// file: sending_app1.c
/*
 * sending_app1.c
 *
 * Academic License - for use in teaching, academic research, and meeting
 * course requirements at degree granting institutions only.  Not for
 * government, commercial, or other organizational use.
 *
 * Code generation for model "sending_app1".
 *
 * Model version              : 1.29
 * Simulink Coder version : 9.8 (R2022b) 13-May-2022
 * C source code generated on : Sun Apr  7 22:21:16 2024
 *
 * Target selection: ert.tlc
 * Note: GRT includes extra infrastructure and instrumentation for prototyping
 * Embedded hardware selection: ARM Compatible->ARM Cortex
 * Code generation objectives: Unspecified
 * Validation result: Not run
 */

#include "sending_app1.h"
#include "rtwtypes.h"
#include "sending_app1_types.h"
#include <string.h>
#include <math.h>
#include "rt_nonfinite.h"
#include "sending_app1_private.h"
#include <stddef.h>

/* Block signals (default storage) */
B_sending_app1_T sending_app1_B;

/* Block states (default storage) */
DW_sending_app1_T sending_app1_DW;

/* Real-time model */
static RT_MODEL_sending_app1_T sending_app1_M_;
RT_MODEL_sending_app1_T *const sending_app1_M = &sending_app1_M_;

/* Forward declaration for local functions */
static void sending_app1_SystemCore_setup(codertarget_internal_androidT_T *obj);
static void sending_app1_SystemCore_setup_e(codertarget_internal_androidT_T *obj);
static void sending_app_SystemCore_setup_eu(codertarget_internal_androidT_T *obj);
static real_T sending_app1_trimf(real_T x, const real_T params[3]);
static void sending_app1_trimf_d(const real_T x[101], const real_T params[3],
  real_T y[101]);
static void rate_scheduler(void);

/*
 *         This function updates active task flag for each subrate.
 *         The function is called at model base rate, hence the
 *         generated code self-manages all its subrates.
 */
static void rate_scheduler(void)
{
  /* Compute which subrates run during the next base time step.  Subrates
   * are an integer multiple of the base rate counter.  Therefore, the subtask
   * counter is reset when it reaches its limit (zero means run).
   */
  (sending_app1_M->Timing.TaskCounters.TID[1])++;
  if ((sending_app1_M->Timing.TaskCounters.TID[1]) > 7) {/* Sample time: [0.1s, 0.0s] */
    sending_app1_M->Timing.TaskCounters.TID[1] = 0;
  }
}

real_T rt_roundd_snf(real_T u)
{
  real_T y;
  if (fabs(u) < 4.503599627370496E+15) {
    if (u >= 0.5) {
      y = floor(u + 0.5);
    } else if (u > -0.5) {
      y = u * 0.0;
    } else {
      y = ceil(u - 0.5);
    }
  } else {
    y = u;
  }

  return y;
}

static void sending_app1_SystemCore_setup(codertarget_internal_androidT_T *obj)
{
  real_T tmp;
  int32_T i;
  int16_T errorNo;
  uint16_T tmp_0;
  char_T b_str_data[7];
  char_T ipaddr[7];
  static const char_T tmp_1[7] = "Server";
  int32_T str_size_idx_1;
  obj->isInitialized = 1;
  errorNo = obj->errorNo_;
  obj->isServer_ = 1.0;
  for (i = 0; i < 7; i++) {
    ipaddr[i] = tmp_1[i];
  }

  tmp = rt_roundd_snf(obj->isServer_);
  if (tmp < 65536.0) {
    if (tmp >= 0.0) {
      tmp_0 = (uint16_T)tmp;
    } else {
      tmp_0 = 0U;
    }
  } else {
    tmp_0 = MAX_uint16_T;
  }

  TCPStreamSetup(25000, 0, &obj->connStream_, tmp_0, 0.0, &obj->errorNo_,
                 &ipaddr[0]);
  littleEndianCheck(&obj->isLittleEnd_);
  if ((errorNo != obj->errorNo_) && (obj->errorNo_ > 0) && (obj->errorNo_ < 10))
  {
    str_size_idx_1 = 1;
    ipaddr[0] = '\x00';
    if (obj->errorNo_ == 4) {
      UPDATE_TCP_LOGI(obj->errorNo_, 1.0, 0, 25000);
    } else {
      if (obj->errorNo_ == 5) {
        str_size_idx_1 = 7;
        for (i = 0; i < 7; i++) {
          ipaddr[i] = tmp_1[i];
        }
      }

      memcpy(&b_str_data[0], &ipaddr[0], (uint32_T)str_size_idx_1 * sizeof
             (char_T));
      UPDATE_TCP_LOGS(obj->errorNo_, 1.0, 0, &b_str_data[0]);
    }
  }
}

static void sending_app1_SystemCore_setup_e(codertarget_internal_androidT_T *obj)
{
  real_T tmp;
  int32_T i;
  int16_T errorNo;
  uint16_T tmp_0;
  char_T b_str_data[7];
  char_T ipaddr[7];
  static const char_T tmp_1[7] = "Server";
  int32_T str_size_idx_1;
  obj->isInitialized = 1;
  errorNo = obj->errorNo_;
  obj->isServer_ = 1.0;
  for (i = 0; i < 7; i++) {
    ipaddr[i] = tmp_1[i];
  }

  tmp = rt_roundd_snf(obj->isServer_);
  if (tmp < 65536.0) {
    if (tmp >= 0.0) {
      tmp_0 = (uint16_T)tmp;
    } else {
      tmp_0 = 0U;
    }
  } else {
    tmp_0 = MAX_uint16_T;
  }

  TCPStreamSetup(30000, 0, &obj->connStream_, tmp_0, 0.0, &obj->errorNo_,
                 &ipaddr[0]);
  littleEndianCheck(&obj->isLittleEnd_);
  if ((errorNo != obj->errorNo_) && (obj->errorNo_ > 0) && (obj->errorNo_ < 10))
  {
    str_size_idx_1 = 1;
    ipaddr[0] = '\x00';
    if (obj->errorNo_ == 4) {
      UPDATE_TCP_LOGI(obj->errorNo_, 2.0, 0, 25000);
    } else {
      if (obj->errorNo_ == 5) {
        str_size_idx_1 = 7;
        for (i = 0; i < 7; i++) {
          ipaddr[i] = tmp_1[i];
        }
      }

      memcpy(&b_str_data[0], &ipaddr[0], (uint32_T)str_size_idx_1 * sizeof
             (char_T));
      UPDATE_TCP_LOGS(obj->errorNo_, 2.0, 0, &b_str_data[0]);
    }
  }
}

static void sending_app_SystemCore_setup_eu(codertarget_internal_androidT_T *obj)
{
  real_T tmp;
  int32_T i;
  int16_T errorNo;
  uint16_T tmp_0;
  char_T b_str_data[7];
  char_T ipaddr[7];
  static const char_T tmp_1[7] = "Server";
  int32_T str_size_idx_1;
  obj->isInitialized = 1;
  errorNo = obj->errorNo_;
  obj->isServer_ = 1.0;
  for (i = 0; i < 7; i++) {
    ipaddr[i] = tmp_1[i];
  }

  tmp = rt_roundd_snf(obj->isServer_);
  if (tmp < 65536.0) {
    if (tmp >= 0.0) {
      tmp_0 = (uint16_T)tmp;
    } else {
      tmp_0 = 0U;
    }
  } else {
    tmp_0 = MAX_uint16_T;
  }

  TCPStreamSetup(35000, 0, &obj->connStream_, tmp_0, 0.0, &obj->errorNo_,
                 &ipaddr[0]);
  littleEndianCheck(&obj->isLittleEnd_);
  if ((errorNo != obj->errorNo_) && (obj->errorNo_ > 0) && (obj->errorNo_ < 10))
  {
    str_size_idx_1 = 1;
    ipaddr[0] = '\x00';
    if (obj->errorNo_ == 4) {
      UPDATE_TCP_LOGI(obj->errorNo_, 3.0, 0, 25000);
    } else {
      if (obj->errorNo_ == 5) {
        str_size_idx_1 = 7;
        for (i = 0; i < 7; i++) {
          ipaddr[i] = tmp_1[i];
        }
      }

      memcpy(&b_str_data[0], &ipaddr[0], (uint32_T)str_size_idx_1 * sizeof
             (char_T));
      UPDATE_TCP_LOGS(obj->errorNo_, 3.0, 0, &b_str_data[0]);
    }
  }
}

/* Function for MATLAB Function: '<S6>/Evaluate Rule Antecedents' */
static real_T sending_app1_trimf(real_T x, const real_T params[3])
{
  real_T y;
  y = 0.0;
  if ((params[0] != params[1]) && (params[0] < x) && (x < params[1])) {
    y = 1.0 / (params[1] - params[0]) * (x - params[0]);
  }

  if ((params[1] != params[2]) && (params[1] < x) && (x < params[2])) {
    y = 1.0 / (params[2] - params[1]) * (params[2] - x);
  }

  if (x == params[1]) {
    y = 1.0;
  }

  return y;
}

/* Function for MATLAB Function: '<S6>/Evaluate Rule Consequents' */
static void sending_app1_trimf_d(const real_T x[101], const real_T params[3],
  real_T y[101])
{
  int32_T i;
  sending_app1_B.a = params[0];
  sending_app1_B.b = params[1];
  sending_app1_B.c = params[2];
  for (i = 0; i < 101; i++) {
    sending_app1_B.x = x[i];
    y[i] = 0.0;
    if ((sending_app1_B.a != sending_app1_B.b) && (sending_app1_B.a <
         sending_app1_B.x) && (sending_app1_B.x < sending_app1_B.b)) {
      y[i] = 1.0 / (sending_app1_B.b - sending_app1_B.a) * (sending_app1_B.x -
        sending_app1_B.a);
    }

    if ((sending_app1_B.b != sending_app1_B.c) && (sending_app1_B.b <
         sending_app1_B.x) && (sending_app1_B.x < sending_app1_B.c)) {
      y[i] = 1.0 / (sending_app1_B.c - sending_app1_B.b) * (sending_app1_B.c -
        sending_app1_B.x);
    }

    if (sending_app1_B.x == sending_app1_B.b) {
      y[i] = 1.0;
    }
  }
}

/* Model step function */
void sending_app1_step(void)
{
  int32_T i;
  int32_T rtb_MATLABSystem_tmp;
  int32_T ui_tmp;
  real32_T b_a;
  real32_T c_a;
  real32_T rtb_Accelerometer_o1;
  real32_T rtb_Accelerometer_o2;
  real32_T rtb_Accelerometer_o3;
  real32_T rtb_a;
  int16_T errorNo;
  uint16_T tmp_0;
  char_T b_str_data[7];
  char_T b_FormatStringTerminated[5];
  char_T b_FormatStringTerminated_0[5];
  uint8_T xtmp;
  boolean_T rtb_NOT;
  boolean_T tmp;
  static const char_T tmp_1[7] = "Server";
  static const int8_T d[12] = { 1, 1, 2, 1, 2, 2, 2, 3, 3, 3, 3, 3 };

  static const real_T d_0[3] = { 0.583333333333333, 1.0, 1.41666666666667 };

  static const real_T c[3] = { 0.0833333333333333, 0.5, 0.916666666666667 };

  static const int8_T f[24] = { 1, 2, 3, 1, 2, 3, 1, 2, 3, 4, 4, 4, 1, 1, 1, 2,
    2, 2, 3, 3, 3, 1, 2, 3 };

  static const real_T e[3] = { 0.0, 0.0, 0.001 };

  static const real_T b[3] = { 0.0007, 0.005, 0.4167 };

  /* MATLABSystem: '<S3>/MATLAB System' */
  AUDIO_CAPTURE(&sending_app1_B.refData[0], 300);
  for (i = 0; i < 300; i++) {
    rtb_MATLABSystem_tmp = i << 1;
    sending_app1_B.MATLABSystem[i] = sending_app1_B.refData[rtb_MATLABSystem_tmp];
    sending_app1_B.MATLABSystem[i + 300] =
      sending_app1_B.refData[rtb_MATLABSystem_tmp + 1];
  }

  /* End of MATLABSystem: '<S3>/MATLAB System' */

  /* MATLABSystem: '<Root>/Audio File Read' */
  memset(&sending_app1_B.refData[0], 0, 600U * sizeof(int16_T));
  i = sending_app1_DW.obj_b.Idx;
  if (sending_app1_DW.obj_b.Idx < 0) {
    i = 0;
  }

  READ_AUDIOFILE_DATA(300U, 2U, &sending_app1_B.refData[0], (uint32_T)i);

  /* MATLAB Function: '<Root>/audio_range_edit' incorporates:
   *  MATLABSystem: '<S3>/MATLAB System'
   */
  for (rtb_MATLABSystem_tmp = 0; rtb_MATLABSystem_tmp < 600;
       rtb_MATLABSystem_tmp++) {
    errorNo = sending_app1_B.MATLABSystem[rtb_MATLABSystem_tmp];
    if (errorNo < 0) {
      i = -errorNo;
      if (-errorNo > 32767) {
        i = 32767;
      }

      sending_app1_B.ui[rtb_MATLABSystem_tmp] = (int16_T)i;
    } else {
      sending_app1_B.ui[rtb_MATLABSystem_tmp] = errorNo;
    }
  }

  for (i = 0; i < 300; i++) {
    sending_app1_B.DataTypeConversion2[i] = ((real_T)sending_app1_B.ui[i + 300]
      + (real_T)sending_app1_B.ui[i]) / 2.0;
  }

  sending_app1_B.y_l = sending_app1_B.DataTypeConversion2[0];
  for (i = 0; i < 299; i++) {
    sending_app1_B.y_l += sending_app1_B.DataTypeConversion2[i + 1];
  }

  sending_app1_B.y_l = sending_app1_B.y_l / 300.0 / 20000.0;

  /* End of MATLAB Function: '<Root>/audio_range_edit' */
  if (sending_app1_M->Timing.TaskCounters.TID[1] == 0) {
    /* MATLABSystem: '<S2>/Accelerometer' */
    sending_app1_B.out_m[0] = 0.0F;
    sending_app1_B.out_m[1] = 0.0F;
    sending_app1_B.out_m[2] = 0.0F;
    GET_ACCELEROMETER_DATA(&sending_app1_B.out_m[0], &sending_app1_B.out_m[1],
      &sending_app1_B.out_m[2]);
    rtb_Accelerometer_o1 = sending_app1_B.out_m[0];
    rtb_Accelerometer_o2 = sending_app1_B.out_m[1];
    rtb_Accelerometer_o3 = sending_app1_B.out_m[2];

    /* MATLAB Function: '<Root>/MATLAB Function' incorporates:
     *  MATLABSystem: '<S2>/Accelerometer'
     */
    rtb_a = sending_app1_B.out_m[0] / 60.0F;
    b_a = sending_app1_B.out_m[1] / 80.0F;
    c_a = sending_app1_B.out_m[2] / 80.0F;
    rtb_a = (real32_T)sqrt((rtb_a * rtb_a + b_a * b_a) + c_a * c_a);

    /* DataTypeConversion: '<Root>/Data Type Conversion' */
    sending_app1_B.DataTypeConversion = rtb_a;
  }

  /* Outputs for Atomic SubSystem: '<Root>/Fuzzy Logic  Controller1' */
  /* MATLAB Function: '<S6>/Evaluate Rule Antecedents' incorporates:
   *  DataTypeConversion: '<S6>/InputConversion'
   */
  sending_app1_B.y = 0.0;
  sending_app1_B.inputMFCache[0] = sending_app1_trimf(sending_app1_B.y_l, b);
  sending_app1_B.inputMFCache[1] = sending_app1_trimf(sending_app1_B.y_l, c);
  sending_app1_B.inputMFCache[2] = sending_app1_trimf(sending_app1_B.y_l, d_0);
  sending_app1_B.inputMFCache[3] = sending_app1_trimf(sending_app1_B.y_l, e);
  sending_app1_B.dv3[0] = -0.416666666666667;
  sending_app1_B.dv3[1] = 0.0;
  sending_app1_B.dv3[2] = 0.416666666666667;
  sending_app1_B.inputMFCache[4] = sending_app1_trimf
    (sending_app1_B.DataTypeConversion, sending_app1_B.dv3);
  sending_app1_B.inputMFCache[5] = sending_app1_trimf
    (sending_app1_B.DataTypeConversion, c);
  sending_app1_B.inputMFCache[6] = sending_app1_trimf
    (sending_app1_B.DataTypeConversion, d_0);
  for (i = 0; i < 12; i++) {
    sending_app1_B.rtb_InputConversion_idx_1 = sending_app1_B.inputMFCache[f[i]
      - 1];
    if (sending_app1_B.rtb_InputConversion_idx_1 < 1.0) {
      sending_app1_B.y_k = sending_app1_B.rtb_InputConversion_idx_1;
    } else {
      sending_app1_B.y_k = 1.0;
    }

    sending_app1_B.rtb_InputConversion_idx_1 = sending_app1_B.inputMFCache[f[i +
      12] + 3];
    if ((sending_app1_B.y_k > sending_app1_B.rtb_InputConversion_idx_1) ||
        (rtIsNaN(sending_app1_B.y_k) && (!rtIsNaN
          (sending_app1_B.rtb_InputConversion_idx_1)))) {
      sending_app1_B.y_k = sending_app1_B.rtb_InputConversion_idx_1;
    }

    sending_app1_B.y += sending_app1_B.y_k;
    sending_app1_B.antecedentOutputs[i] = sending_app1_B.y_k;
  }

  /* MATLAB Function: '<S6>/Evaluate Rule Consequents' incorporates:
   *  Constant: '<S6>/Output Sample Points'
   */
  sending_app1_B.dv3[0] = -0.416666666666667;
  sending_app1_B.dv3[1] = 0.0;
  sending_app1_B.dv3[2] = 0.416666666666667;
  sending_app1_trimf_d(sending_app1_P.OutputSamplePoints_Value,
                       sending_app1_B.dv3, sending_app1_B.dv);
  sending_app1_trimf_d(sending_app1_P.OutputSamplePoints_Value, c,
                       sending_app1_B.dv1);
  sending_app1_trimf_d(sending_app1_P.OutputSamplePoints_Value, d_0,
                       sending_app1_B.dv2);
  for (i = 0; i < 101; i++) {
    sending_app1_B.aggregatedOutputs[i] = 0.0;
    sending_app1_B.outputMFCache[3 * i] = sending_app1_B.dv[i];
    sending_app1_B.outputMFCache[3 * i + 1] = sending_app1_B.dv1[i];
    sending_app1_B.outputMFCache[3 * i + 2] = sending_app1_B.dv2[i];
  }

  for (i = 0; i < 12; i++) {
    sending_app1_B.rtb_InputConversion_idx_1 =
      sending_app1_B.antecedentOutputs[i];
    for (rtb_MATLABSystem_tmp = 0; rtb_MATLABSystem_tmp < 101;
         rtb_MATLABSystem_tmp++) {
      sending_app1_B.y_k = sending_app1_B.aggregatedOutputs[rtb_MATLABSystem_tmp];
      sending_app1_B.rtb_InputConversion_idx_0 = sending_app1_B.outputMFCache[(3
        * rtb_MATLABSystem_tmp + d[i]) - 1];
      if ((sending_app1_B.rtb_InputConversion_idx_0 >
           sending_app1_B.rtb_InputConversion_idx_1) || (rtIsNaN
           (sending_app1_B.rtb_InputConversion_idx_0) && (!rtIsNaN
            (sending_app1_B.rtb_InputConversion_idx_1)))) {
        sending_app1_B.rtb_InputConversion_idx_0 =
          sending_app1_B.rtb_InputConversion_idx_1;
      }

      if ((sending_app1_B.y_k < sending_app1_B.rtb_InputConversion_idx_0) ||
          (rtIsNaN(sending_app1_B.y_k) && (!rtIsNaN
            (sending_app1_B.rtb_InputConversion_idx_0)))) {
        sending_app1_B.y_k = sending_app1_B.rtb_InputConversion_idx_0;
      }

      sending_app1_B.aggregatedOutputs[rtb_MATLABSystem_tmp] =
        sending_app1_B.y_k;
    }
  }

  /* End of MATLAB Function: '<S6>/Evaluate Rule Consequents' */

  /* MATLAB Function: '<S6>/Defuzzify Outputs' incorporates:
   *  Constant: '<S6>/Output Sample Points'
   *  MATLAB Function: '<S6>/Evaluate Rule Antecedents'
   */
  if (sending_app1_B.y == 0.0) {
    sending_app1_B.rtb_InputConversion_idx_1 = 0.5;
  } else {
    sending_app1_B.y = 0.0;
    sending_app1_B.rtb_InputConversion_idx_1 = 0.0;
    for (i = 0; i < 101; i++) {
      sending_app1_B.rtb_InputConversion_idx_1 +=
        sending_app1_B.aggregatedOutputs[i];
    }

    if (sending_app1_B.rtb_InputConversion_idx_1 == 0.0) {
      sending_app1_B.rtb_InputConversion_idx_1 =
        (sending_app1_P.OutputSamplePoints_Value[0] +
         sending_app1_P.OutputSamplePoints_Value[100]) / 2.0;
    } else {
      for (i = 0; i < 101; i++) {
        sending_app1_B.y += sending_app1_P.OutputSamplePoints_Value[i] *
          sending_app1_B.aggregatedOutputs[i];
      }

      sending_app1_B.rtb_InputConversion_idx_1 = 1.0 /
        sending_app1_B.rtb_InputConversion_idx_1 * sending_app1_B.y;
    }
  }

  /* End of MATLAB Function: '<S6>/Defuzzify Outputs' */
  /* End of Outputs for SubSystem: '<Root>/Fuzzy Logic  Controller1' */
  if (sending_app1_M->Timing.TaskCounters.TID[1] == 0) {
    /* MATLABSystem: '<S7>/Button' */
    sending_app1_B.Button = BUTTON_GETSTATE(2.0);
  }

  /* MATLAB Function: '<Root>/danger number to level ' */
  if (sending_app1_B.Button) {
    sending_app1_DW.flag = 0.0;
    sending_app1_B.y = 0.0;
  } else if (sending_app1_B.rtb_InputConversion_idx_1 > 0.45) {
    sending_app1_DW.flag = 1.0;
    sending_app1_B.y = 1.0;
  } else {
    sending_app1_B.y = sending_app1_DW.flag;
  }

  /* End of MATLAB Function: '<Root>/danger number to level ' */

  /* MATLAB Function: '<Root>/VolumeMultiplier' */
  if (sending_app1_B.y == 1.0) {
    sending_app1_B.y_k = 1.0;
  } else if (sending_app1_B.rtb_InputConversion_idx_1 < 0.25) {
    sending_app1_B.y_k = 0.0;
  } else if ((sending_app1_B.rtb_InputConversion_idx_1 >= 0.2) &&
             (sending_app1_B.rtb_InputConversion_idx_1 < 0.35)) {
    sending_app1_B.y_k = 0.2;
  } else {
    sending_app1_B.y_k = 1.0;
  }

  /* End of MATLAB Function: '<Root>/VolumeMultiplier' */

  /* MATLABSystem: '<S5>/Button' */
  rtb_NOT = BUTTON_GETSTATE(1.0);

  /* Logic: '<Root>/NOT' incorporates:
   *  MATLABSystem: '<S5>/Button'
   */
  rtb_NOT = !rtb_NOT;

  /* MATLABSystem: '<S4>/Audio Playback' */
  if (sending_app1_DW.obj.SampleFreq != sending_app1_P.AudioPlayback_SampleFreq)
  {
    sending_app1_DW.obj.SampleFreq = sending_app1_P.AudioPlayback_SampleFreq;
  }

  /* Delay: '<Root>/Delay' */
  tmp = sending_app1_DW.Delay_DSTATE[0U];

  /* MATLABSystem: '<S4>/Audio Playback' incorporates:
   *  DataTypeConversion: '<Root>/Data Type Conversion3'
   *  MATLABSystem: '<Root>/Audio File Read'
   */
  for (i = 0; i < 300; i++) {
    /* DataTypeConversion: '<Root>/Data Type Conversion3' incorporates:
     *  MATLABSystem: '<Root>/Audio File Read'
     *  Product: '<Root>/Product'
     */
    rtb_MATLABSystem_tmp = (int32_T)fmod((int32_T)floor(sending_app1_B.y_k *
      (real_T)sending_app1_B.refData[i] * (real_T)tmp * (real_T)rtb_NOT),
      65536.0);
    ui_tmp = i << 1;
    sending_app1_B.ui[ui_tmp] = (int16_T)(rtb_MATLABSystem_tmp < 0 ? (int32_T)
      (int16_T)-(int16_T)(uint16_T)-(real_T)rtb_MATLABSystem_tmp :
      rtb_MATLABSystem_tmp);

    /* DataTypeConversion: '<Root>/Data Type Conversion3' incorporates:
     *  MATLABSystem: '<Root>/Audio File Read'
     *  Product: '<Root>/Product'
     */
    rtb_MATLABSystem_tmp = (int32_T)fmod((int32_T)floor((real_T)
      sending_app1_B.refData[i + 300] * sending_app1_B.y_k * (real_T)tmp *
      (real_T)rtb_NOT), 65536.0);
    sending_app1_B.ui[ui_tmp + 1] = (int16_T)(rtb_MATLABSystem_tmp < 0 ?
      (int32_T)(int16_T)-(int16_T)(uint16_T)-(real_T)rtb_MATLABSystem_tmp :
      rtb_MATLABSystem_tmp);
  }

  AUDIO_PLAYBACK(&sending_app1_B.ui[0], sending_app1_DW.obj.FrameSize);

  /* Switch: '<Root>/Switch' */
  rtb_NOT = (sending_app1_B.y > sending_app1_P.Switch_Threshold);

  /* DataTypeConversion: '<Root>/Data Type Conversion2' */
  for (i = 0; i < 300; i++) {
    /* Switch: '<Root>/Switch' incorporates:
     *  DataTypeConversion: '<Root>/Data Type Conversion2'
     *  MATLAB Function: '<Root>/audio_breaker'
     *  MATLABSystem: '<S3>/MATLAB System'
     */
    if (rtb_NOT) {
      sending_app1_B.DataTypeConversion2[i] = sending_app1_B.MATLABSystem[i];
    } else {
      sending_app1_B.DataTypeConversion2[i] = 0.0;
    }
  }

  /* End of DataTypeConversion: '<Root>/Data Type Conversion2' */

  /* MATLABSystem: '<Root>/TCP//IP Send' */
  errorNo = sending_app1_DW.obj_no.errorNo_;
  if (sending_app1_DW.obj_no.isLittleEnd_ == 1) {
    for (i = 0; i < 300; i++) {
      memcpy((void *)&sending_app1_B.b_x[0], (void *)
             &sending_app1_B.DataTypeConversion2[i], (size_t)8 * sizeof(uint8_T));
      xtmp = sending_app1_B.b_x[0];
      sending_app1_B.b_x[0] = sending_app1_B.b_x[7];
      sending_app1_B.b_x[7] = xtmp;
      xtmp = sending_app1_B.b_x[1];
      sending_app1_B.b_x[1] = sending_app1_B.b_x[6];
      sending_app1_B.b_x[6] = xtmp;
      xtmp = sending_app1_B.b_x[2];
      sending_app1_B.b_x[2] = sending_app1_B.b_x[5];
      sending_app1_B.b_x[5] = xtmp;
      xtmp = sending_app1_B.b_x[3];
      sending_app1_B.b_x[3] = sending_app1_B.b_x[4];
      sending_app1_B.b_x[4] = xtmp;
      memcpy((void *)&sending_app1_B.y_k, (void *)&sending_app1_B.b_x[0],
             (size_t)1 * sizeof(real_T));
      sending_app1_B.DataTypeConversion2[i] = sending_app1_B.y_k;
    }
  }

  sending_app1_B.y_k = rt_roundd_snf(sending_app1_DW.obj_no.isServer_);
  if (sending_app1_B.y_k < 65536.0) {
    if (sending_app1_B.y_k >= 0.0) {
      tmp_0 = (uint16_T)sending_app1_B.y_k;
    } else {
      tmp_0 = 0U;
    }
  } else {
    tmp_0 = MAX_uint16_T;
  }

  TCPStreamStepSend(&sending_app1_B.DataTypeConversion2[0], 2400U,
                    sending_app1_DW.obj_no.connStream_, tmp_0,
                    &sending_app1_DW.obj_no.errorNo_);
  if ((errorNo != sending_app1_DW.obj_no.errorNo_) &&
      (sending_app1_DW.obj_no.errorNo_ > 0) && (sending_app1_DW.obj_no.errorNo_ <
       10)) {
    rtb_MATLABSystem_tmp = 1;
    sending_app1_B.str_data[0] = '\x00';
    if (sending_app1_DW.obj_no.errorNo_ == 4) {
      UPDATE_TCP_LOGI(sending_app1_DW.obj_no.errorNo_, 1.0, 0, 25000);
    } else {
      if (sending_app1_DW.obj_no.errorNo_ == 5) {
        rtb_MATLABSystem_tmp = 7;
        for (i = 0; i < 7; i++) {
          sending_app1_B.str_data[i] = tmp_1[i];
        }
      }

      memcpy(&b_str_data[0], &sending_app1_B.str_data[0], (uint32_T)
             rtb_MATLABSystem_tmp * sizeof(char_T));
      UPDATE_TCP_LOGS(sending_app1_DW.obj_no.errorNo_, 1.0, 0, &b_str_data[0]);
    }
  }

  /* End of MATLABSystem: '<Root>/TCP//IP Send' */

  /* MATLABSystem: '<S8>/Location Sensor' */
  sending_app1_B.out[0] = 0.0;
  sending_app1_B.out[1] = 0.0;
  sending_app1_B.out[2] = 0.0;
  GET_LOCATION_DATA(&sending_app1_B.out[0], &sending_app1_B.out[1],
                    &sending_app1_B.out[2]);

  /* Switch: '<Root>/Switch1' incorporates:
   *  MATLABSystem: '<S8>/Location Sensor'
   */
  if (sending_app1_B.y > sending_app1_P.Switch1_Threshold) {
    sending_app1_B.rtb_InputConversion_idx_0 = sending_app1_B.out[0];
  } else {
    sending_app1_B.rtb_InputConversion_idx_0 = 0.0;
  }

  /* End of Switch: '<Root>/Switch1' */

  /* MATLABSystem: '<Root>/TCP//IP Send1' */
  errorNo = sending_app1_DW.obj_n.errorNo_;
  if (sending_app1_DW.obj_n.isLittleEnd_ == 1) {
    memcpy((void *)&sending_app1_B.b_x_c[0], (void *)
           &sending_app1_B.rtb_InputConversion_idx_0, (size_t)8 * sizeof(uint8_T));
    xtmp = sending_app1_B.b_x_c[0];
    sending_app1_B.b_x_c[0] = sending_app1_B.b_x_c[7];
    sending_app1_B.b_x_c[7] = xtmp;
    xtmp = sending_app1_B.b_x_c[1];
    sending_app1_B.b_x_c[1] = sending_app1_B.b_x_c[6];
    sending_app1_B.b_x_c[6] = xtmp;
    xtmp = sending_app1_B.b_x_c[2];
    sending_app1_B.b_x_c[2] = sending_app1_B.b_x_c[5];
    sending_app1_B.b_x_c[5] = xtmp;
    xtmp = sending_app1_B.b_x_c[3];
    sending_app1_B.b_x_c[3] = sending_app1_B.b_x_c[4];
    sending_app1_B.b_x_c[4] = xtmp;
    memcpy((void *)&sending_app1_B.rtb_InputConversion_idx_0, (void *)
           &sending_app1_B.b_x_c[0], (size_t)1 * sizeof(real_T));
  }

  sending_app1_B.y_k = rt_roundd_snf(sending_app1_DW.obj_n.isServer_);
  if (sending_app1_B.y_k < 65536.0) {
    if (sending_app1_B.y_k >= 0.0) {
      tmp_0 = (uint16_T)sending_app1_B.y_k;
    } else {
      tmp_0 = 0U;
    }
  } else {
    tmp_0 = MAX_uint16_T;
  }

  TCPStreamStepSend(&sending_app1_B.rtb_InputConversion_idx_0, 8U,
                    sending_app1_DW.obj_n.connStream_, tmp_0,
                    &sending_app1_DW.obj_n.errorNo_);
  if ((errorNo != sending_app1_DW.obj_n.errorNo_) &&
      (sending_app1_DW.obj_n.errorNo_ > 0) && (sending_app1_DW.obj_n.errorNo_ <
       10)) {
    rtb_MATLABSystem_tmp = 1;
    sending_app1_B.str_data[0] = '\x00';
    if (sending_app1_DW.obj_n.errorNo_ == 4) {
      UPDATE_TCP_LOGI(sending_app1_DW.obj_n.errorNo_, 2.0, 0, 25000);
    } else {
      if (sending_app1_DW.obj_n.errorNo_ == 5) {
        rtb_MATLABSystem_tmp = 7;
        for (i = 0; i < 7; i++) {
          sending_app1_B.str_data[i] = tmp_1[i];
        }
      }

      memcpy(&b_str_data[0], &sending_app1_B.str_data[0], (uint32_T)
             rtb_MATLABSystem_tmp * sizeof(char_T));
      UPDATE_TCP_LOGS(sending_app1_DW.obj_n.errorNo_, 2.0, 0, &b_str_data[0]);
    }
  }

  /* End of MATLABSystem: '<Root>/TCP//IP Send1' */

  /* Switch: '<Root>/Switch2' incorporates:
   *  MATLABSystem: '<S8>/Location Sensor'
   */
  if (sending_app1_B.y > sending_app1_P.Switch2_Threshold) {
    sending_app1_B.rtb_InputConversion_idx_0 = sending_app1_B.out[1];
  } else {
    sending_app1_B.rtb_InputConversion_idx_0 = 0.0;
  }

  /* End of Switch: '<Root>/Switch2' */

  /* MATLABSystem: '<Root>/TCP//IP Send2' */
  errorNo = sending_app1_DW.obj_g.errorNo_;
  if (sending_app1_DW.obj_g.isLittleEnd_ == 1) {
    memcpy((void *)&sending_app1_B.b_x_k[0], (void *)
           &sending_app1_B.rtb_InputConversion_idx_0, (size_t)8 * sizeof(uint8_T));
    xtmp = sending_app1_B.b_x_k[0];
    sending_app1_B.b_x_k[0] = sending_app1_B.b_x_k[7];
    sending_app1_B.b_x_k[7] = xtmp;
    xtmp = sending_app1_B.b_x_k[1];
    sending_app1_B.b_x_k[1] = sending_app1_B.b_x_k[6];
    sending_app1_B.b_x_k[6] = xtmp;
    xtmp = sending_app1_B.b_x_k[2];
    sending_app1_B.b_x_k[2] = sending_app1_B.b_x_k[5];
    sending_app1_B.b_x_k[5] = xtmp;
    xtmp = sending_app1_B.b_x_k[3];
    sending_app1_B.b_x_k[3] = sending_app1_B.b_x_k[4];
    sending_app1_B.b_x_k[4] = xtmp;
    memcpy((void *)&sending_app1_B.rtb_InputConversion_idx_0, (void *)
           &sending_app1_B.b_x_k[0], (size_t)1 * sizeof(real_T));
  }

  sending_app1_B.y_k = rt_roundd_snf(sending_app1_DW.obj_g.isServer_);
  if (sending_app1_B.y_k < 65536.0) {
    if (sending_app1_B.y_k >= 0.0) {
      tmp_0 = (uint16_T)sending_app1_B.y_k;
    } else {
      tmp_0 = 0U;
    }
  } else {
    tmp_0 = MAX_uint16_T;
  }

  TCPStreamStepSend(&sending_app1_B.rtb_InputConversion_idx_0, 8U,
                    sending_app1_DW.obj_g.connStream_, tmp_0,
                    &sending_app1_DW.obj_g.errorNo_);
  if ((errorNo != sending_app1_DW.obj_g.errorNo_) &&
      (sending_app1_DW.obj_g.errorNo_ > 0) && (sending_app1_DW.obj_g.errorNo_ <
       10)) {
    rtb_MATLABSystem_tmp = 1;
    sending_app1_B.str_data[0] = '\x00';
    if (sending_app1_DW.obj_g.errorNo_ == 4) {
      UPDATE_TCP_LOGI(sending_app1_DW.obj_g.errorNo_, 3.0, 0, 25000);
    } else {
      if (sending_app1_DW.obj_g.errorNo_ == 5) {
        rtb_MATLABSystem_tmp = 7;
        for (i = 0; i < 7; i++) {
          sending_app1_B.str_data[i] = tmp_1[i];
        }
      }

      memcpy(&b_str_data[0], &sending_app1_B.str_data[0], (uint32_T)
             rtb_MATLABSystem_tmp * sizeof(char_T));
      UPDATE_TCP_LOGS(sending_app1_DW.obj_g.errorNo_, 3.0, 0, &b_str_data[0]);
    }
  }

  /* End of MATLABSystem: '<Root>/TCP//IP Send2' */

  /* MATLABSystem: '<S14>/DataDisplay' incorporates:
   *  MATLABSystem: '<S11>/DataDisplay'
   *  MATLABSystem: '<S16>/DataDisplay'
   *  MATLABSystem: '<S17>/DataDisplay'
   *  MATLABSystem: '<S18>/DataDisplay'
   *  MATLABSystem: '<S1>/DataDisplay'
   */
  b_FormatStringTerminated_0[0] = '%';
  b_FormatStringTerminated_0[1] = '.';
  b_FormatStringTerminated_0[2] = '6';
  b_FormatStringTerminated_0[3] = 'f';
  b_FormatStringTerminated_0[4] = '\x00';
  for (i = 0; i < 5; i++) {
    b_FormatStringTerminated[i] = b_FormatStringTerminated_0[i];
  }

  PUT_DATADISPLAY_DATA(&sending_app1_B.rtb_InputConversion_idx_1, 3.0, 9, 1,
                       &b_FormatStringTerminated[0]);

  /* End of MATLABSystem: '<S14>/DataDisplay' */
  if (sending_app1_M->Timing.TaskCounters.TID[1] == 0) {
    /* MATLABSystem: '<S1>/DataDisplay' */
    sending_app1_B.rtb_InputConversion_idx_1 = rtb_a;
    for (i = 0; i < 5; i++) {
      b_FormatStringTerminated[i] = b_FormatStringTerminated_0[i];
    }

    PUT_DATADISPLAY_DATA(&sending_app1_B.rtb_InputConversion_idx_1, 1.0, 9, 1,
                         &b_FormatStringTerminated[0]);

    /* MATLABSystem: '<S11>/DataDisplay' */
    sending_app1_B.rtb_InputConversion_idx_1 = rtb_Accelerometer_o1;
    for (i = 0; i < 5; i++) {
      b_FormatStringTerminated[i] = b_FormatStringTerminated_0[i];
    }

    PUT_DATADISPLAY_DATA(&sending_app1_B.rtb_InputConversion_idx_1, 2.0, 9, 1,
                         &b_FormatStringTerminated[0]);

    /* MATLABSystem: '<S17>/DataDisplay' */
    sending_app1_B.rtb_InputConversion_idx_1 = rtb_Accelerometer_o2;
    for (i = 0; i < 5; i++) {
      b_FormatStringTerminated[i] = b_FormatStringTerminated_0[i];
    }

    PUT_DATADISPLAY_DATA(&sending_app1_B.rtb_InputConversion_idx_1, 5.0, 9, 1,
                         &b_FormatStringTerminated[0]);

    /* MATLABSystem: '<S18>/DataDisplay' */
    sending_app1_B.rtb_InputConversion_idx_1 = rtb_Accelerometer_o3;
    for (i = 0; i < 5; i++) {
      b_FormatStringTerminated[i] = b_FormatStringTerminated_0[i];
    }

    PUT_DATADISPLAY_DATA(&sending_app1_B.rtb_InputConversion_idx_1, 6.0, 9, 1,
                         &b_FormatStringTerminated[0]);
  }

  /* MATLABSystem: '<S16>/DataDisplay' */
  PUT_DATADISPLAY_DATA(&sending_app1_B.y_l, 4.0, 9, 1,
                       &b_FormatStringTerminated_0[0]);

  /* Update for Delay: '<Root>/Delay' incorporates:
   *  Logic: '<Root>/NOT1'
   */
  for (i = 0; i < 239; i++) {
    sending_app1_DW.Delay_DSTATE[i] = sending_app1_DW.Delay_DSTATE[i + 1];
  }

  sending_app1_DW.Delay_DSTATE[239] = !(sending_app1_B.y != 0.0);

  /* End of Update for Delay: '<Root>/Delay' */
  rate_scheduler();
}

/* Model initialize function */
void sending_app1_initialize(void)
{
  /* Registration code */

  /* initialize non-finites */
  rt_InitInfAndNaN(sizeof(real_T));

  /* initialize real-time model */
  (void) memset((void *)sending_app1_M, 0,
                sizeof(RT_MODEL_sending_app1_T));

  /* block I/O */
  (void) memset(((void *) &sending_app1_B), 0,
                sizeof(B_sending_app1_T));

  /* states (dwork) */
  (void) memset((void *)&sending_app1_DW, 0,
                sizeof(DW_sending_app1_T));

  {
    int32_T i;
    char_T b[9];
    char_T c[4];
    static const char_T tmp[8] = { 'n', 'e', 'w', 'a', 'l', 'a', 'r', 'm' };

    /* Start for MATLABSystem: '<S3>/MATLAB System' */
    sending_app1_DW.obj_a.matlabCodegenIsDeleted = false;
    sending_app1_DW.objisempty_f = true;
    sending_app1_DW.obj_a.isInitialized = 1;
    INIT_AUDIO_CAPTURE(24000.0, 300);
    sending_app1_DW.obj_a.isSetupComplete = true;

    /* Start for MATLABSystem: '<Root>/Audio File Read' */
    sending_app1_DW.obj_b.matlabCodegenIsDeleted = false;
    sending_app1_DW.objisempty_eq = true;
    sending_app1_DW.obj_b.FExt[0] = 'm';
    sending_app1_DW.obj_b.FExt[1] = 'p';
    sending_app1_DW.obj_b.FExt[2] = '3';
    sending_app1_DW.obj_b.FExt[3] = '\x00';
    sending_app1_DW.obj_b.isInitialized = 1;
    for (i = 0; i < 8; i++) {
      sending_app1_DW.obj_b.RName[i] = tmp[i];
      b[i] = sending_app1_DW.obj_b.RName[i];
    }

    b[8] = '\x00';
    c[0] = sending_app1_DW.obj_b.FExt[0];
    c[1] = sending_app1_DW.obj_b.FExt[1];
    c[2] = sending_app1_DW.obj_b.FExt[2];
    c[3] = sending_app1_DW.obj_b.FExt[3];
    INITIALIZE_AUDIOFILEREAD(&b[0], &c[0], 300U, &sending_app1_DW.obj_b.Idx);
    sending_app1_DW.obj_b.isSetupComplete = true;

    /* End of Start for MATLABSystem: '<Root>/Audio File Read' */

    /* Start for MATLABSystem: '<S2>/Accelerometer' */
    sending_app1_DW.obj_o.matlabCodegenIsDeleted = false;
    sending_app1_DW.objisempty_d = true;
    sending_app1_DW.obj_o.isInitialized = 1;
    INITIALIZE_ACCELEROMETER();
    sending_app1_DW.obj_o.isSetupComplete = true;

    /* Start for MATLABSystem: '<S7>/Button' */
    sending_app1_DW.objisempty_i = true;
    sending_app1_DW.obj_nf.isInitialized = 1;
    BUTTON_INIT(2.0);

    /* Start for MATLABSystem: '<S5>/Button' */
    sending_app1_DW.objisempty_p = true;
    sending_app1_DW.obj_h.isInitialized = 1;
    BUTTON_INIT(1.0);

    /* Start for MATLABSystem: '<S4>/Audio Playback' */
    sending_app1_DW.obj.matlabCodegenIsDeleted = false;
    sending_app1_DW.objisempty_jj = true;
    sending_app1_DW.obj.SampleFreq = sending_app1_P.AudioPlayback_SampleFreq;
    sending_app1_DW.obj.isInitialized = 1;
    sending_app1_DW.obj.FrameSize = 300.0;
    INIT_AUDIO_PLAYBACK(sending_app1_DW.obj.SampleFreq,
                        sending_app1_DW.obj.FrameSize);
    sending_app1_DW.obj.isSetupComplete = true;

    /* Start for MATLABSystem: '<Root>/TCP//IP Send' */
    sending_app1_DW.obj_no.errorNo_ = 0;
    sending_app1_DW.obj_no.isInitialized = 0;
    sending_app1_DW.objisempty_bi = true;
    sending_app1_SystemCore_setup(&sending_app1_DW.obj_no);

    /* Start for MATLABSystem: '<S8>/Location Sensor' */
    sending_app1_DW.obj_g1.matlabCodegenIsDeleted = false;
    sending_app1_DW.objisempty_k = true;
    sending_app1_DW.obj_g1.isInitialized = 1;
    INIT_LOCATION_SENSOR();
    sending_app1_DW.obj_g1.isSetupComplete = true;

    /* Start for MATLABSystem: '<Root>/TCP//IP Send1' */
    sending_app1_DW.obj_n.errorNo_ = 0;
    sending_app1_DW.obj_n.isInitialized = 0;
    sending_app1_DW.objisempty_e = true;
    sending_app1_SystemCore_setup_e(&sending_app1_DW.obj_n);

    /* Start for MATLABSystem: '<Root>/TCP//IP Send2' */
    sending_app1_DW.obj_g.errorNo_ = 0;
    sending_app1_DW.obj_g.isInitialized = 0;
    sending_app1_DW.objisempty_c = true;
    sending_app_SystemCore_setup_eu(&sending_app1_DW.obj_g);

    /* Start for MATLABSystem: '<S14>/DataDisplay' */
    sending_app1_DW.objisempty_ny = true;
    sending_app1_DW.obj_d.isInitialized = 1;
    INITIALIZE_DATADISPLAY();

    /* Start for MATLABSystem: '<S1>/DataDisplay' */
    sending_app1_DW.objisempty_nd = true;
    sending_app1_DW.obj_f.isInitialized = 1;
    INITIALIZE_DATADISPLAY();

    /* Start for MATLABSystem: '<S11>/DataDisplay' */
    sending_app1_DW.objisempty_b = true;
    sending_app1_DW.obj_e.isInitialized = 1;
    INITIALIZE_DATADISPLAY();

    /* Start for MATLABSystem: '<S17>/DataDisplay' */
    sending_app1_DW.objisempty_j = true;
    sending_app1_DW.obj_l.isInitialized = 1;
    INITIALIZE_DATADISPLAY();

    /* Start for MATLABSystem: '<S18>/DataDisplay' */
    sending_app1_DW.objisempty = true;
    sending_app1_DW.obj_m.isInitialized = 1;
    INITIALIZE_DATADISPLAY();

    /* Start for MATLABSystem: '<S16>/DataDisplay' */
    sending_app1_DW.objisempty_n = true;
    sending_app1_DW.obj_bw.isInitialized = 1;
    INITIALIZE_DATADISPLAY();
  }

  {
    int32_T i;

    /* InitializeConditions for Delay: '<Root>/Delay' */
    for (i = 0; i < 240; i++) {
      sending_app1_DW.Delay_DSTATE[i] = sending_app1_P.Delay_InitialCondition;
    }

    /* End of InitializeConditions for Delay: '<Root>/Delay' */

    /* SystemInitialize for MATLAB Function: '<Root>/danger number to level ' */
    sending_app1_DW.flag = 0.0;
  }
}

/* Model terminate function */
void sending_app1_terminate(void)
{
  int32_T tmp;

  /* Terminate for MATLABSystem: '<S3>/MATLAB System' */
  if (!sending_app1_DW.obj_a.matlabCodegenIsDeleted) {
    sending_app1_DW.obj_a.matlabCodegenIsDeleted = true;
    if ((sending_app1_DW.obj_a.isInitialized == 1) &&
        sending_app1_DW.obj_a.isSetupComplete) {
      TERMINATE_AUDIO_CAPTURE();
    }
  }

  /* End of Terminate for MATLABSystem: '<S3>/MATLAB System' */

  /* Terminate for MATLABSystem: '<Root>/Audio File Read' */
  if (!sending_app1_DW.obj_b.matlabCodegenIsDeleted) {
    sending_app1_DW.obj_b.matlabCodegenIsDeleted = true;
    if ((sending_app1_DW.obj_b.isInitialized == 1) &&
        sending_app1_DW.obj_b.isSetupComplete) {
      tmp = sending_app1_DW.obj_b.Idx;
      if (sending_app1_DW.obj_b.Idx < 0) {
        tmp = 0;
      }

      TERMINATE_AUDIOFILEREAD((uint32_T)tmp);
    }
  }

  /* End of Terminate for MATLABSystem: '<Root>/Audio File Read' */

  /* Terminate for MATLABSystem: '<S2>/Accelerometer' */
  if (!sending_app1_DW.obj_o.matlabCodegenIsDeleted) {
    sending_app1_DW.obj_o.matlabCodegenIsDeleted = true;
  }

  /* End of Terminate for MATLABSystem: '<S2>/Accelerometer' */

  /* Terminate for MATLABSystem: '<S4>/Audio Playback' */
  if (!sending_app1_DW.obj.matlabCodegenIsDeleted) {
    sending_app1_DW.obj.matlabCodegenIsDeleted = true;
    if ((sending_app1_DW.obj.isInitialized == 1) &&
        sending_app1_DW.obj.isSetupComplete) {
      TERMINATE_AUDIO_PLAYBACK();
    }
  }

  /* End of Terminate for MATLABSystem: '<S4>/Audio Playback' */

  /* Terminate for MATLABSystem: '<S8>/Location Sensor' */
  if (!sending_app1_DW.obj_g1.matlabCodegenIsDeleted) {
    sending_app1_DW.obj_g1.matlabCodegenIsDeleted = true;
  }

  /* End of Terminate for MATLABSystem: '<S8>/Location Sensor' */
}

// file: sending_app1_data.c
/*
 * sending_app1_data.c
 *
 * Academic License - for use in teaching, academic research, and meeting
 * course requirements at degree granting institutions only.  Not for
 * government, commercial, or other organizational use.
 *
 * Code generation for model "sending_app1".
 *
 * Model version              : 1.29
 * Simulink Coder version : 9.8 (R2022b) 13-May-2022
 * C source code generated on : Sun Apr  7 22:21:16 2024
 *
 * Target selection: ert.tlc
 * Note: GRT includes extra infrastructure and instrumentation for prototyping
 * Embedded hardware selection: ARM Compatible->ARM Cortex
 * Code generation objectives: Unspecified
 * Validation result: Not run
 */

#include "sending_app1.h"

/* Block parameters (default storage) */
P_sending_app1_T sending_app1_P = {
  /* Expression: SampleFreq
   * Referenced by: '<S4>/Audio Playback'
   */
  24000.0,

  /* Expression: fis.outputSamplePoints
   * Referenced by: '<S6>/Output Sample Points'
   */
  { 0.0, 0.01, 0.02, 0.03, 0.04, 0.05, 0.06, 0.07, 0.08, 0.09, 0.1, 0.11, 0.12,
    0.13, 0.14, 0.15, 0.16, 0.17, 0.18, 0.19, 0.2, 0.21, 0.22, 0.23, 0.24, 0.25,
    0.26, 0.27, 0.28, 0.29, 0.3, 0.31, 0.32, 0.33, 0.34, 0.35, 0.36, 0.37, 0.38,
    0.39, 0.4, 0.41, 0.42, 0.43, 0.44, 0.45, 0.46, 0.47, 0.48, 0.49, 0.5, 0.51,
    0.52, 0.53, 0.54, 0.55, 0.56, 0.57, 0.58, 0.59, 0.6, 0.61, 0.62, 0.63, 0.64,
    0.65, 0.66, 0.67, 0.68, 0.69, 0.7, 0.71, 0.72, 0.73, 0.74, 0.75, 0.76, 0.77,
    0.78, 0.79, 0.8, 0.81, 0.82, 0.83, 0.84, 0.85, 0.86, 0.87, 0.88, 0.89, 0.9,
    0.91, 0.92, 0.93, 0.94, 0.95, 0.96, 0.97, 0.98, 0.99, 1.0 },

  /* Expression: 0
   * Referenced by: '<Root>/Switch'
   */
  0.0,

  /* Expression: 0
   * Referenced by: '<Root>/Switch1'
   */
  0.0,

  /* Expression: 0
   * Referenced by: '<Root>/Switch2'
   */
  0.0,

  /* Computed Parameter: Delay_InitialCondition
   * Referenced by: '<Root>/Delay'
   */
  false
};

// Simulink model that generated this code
simulink model "sending_app1"  (R2022b)
settings: Solver=FixedStepAuto  StartTime=0.0  StopTime=inf  FixedStep=0.0125  RelTol=1e-3
libraries: androiduilib x8, androidaudiovideolib x3, androidcommunicationlib x3, androidsensorlib x2, fuzblock x1

== system sending_app1 ==
  note: Audio Transmission
  note: Fuzzy Logic Control
  note: Alarm Playback with Volume Multiplier
  note: GPS Data Collection and Transmission
  note: Accelerometer Data Collection
  Acceleration : androiduilib/Data Display  DataDisplayId=sending_app1/Acceleration  Format=Float  Precision=6  SimulateUsing=Code generation  blockPlatform=Android
  Accelerometer : androidsensorlib/Accelerometer  OutputVector=off  SampleTime=0.1  BlockPlatform=Android
  Audio Capture : androidaudiovideolib/Audio Capture  SampleFreq=24000  FrameSize=300  SampleTime=0.0125  SimulateUsing=Code generation  DeviceStr=0  QueueDuration=0  BlockPlatform=Android  AudioSamplingFreq=44100
  Audio File Read : androidaudiovideolib/Audio File Read  FileName=D:\Courses\ES245_ControlSystems\newalarm.mp3  FrameSize=300
  Audio Playback : androidaudiovideolib/Audio Playback  SampleFreq=24000  AudioSamplingFreq=24000  SampleTime=0.1  DeviceStr=0  QueueDuration=0  BlockPlatform=Android
  Bus Creator : BusCreator  Inputs=2
  Data Type Conversion{,1..2,4..5} (5 alike) : DataTypeConversion  OutDataTypeStr=double  SaturateOnIntegerOverflow=off  RndMeth=Floor
  Data Type Conversion3 : DataTypeConversion  OutDataTypeStr=int16  SaturateOnIntegerOverflow=off  RndMeth=Floor
  Delay : Delay  DelayLength=240
  Dont ring : androiduilib/Button  ButtonState=Not pressed  ButtonId=sending_app1/Dont_ring  State=off  SampleTime=0.0125  BlockPlatform=Android
  Fuzzy Logic Controller1 : fuzblock/Fuzzy Logic  Controller  FIS=fuzzy_verylow  OutputSampleNumber=101  DataType=double  FuzzifiedInputs=off  RuleFiringStrengths=off  RuleOutputs=off  AggregatedOutputs=off  SimulateUsing=Interpreted execution  OutOfRangeInputValueMessage=warning  NoRuleFiredMessage=warning  EmptyOutputFuzzySetMessage=warning
  I am Fine! (for now) : androiduilib/Button  ButtonState=Not pressed  ButtonId=sending_app1/I_am_Fine!_(for_now)  State=off  SampleTime=0.1  BlockPlatform=Android
  Location Sensor : androidsensorlib/Location Sensor  OutputVector=off  SampleTime=0.0125  BlockPlatform=Android
  MATLAB Function : MATLAB Function  TreatAsAtomicUnit=on
  NOT : Logic  Operator=NOT  IconShape=distinctive  AllPortsSameDT=off  OutDataTypeStr=boolean
  NOT1 : Logic  Operator=NOT  IconShape=distinctive  AllPortsSameDT=off  OutDataTypeStr=boolean
  Product : Product  Inputs=4
  Switch : Switch  Criteria=u2 > Threshold  SaturateOnIntegerOverflow=off  InputSameDT=off
  Switch1 : Switch  Criteria=u2 > Threshold  OutDataTypeStr=double  SaturateOnIntegerOverflow=off  InputSameDT=off
  Switch2 : Switch  Criteria=u2 > Threshold  OutDataTypeStr=double  SaturateOnIntegerOverflow=off  InputSameDT=off
  TCP/IP Send : androidcommunicationlib/TCP//IP Send  TCPSendId=sending_app1/TCP//IP_Send  Mode_=Server  LocalServerPort_=25000  RemoteAddr_=10.7.21.239  RemoteServerPort_=25000  ClientPortBindingSelection_=off  ClientPortToBind_=35000  BlockingMode_=off  BlockTimeout_=0.1
  TCP/IP Send1 : androidcommunicationlib/TCP//IP Send  TCPSendId=sending_app1/TCP//IP_Send1  Mode_=Server  LocalServerPort_=30000  RemoteAddr_=127.0.0.1  RemoteServerPort_=25000  ClientPortBindingSelection_=off  ClientPortToBind_=35000  BlockingMode_=off  BlockTimeout_=0.1
  TCP/IP Send2 : androidcommunicationlib/TCP//IP Send  TCPSendId=sending_app1/TCP//IP_Send2  Mode_=Server  LocalServerPort_=35000  RemoteAddr_=127.0.0.1  RemoteServerPort_=25000  ClientPortBindingSelection_=off  ClientPortToBind_=35000  BlockingMode_=off  BlockTimeout_=0.1
  VolumeMultiplier : MATLAB Function  TreatAsAtomicUnit=on
  X : androiduilib/Data Display  DataDisplayId=sending_app1/X  Format=Float  Precision=6  SimulateUsing=Code generation  blockPlatform=Android
  audio_breaker : MATLAB Function  TreatAsAtomicUnit=on
  audio_range_edit : MATLAB Function  TreatAsAtomicUnit=on
  danger : androiduilib/Data Display  DataDisplayId=sending_app1/danger  Format=Float  Precision=6  SimulateUsing=Code generation  blockPlatform=Android
  "danger number to level " : MATLAB Function  TreatAsAtomicUnit=on
  sound : androiduilib/Data Display  DataDisplayId=sending_app1/sound  Format=Float  Precision=6  SimulateUsing=Code generation  blockPlatform=Android
  y : androiduilib/Data Display  DataDisplayId=sending_app1/y  Format=Float  Precision=6  SimulateUsing=Code generation  blockPlatform=Android
  z : androiduilib/Data Display  DataDisplayId=sending_app1/z  Format=Float  Precision=6  SimulateUsing=Code generation  blockPlatform=Android
  wires:
  Accelerometer/1 -> MATLAB Function/1(x), X/1
  Accelerometer/2 -> MATLAB Function/2(y), y/1
  Accelerometer/3 -> MATLAB Function/3(z), z/1
  MATLAB Function/1(a) -> Data Type Conversion/1, Acceleration/1
  Bus Creator/1 -> Fuzzy Logic Controller1/1
  Audio Capture/1 -> audio_breaker/1(u), audio_range_edit/1(u)
  audio_range_edit/1(y) -> Data Type Conversion1/1, sound/1
  Data Type Conversion/1 -> Bus Creator/2
  Data Type Conversion1/1 -> Bus Creator/1
  Switch/1 -> Data Type Conversion2/1
  "danger number to level "/1(y) -> NOT1/1, VolumeMultiplier/2(v), Switch/2, Switch1/2, Switch2/2
  audio_breaker/1(y) -> Switch/1
  Data Type Conversion2/1 -> TCP/IP Send/1
  I am Fine! (for now)/1 -> "danger number to level "/1(u)
  VolumeMultiplier/1(y) -> Product/1
  Product/1 -> Data Type Conversion3/1
  Audio File Read/1 -> Product/2
  Data Type Conversion3/1 -> Audio Playback/1
  Dont ring/1 -> NOT/1
  NOT/1 -> Product/4
  Switch1/1 -> Data Type Conversion4/1
  Location Sensor/1 -> Switch1/1
  Data Type Conversion4/1 -> TCP/IP Send1/1
  Switch2/1 -> Data Type Conversion5/1
  Data Type Conversion5/1 -> TCP/IP Send2/1
  Location Sensor/2 -> Switch2/1
  NOT1/1 -> Delay/1
  Fuzzy Logic Controller1/1 -> VolumeMultiplier/1(u), "danger number to level "/2(v), danger/1
  Delay/1 -> Product/3

== matlab function sending_app1/MATLAB Function ==
function a = fcn(x,y,z)
x = x/60;
y = y/80;
z = z/80;

ai = (x^2)+(y^2)+(z^2);
b = ai^0.5;
a = b;

== matlab function sending_app1/audio_breaker ==
function y = fcn(u)
y = u(:,1);

== matlab function sending_app1/danger number to level  ==
function y = fcn(u,v)
persistent flag;

    if isempty(flag)
        flag = 0;
    end

    if u == 1
        flag = 0;
        y = 0;
    elseif v > 0.45
        flag = 1;
        y = 1;
    else
        y = flag;
    end
end

== matlab function sending_app1/VolumeMultiplier ==
function y = fcn(u, v)
    if v ==1
               y = 1;
    elseif u < 0.25
        y = 0;
    elseif u >= 0.20 && u < 0.35
        y = 0.2;
    else
        y = 1;
    end

== matlab function sending_app1/audio_range_edit ==
function y = fcn(u)
ui = abs(u);
yi = mean(ui,2);
y = mean(yi)/20000;
